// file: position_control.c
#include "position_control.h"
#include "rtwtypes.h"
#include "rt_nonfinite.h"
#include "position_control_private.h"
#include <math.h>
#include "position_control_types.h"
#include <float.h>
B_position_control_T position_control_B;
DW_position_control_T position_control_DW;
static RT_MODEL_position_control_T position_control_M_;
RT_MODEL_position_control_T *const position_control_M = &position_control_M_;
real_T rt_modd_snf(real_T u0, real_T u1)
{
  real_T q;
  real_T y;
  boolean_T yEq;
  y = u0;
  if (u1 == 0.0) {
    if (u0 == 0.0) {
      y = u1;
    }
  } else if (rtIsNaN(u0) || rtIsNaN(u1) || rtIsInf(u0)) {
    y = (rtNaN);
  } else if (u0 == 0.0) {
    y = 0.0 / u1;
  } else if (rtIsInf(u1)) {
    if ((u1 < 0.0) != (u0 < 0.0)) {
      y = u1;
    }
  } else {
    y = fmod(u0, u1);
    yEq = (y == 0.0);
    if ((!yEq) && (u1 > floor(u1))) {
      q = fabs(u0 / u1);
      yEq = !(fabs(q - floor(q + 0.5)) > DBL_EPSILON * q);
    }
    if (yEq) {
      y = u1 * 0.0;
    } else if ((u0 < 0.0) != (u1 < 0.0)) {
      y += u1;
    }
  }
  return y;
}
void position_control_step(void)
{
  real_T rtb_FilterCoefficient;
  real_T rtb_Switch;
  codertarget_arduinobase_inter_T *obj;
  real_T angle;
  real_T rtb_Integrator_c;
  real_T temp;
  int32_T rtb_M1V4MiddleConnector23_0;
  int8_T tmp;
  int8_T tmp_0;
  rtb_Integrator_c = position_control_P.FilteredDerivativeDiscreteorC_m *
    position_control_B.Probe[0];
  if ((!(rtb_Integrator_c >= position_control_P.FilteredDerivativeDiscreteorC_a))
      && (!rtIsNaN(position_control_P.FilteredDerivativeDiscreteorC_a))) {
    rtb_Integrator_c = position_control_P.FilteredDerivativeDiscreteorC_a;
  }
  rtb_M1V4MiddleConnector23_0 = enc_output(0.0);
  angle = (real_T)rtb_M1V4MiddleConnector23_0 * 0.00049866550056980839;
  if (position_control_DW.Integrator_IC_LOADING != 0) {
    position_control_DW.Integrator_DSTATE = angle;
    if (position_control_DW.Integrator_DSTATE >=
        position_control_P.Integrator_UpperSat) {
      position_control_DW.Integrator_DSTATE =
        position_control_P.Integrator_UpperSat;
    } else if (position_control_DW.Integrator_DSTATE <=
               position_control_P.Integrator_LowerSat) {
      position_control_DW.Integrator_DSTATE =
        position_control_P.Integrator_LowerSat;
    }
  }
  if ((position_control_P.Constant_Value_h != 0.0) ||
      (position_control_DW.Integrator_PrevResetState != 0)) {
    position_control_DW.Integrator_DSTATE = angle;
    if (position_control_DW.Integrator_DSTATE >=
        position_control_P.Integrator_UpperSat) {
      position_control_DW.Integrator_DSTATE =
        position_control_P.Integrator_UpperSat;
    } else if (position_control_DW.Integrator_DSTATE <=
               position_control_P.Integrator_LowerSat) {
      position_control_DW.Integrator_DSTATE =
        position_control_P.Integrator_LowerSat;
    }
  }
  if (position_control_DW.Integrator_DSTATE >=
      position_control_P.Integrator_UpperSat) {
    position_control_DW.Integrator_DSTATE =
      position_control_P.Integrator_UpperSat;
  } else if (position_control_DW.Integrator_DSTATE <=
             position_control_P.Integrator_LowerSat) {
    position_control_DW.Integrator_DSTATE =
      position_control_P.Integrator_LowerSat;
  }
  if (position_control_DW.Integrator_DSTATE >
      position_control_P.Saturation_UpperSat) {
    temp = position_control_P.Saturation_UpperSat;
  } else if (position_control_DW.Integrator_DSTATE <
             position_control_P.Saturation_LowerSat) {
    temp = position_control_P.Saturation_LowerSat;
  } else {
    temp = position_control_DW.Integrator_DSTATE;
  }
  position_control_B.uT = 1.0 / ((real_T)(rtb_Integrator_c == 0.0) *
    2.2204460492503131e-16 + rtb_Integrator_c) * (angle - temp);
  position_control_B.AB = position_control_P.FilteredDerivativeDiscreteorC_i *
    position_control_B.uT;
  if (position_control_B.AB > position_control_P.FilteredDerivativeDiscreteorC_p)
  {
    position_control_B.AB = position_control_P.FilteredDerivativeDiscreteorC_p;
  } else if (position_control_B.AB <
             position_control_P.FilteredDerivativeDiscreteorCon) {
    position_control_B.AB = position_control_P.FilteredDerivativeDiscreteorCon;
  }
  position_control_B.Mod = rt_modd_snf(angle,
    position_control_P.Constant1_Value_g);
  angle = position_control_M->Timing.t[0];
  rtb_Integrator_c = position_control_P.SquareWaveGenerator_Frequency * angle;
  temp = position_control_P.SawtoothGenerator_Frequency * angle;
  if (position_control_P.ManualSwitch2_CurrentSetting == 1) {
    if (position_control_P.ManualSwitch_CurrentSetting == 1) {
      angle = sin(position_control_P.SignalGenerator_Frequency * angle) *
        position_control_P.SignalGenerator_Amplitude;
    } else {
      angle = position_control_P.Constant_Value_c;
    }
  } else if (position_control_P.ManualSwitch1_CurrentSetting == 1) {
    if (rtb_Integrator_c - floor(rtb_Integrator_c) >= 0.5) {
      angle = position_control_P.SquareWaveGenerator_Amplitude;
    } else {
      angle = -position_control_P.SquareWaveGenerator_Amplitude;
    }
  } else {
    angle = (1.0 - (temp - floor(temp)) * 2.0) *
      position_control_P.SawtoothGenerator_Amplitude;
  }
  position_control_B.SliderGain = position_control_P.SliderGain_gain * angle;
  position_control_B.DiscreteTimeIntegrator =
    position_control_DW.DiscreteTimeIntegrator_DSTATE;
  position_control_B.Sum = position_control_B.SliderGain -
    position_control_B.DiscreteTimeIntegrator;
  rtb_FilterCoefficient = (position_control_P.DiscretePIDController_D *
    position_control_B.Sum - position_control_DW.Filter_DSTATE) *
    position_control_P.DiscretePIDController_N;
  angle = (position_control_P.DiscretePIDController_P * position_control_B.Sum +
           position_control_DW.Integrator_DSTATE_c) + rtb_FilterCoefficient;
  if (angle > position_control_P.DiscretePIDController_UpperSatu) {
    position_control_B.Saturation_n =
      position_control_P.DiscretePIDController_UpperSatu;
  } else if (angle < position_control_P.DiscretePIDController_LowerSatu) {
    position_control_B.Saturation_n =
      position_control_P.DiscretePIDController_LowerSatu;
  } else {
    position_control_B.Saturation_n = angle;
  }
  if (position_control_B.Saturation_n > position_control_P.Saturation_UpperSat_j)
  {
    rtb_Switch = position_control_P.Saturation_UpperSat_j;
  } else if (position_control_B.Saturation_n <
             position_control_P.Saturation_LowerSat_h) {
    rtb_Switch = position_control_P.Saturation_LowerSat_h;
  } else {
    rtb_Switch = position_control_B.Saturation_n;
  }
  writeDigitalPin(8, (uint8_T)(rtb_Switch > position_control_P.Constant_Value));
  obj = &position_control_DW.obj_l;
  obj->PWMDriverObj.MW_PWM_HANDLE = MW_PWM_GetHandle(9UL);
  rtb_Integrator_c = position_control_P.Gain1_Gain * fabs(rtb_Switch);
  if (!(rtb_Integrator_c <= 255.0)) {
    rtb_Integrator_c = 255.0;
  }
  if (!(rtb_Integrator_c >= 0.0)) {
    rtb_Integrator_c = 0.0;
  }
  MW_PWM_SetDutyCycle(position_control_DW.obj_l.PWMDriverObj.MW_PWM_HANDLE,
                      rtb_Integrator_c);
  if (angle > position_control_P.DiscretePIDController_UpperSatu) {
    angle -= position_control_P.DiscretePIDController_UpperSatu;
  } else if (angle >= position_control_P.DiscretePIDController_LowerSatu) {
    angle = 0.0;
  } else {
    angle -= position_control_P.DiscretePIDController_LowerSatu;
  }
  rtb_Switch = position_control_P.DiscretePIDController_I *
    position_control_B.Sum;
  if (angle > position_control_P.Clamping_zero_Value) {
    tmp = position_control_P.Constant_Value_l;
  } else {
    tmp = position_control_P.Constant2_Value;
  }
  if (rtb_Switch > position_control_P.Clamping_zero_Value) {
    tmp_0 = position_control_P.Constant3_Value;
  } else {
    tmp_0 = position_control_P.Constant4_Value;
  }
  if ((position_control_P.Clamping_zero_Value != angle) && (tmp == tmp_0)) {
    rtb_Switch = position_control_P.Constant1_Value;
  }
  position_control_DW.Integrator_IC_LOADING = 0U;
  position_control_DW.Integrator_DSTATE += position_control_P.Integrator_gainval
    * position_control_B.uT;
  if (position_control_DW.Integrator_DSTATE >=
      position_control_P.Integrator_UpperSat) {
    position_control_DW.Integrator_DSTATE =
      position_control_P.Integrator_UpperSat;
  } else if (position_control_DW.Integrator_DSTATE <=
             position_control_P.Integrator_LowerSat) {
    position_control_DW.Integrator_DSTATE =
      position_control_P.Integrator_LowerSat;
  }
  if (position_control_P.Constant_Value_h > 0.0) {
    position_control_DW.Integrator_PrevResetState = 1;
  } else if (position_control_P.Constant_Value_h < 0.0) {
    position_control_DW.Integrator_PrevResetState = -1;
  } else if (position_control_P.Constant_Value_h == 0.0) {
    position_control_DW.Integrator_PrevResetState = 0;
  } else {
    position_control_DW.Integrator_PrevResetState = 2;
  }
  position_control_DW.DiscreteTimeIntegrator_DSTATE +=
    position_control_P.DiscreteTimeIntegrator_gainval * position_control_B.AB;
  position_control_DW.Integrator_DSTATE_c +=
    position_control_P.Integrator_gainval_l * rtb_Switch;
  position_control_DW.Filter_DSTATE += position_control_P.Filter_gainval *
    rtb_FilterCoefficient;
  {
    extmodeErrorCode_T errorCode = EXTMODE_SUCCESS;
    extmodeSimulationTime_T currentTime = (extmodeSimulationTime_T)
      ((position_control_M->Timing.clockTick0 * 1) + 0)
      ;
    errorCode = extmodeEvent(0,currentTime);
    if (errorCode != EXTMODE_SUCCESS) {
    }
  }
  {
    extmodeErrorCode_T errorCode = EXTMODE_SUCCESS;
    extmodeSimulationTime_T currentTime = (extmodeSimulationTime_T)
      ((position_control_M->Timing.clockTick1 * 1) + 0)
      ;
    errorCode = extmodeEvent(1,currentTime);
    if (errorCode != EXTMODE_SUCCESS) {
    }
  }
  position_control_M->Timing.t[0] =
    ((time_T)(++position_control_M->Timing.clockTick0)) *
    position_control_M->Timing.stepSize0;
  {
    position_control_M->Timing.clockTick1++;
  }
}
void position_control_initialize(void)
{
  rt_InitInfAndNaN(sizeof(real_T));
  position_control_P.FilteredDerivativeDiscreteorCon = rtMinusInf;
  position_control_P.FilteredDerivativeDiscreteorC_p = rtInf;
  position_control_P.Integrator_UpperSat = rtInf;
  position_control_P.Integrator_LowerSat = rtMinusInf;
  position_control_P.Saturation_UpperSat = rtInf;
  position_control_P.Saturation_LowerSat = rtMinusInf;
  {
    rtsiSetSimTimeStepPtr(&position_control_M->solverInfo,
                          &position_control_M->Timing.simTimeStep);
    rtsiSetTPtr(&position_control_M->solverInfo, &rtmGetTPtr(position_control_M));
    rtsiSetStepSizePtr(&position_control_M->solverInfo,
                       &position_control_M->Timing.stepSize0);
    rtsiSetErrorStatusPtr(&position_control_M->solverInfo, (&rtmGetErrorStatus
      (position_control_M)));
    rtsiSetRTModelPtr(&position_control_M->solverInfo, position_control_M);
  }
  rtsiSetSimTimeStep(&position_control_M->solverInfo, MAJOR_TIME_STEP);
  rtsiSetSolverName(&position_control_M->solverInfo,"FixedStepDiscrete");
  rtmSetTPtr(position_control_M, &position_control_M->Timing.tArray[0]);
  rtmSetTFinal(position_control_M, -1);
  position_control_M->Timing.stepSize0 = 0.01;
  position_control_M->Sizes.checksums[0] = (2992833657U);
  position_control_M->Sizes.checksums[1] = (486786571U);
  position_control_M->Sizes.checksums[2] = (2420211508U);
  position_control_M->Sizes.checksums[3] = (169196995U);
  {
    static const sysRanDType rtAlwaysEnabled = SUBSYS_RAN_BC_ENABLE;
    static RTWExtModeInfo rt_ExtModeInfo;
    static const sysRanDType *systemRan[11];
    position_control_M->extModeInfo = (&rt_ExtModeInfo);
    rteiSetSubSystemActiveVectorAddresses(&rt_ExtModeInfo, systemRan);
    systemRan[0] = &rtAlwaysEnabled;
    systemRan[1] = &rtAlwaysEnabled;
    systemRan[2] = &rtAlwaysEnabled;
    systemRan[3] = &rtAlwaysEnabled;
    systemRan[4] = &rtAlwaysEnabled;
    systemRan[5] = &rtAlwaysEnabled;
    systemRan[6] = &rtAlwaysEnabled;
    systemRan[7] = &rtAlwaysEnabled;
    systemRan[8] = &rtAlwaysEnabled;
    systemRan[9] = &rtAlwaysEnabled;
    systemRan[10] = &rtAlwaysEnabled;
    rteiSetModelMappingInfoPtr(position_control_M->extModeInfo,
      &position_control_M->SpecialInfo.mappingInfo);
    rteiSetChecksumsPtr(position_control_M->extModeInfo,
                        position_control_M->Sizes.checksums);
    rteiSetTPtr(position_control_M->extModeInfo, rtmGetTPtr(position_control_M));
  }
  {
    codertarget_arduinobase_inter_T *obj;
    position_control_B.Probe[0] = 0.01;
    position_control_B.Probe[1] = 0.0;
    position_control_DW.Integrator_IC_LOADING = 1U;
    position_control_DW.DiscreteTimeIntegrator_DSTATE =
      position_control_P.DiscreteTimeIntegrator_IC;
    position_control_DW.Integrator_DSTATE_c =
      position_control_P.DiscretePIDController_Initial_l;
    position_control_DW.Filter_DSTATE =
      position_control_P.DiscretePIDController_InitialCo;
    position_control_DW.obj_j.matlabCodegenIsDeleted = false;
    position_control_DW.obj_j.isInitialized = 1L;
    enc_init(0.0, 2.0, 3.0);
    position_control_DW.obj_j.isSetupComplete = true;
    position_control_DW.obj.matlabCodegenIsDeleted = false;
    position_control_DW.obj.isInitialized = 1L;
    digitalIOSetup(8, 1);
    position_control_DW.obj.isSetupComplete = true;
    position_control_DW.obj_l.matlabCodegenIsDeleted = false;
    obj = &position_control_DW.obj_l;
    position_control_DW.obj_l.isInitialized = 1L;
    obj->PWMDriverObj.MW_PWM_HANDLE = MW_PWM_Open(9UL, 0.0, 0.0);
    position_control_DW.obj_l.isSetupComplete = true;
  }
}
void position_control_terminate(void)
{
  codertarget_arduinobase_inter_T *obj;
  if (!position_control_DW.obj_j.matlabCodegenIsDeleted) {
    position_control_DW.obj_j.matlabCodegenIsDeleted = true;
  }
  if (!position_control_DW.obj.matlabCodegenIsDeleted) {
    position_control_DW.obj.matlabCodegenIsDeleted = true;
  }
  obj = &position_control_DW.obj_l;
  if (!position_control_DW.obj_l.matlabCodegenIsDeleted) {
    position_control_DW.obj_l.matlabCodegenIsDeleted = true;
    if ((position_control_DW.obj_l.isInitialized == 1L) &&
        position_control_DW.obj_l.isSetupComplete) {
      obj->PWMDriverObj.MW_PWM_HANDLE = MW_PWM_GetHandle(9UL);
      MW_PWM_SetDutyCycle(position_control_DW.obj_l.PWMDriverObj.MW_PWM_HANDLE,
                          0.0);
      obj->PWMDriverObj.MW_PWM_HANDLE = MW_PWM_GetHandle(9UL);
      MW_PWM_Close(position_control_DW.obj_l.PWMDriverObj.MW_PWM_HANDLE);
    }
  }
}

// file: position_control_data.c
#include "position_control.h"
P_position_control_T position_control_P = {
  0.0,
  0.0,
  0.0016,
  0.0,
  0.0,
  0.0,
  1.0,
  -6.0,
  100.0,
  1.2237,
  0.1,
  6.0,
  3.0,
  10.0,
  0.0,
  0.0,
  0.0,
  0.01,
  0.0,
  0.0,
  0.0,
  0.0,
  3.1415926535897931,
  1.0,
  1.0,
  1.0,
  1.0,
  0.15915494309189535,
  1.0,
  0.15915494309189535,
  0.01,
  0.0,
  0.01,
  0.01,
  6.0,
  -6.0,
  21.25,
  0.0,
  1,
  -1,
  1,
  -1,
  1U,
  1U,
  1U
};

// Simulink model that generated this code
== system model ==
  Mod : Math  Operator=mod  <- 1: MATLABFunction#1, 2: Constant1
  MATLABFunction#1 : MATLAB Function  <- 1: DataTypeConversion#1
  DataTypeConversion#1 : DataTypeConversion  <- 1: M1V4MiddleConnector23
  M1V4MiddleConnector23 : MinSegLibrary_M1V4/M1V4 Middle Connector 2,3
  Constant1 : Constant  Value=pi
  DigitalOutput#1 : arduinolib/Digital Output  pinNumber=8  <- 1: CompareToZero#1
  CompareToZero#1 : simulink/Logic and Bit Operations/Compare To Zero  relop=>  <- 1: Saturation
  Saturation : Saturate  UpperLimit=6  LowerLimit=-6  <- 1: DiscretePIDController
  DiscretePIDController : slpidlib/PID Controller  Controller=PID  Form=Parallel  TimeDomain=Discrete-time  IntegratorMethod=Forward Euler  P=1.2237  I=0  D=0.0016  N=100  InitialConditionForIntegrator=0  ExternalReset=none  LimitOutput=on  UpperSaturationLimit=6  LowerSaturationLimit=-6  <- 1: Sum
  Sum : Sum  Inputs=+-  <- 1: SliderGain, 2: DiscreteTimeIntegrator
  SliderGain : simulink/Math Operations/Slider Gain  <- 1: ManualSwitch2
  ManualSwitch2 : ManualSwitch  <- 1: ManualSwitch, 2: ManualSwitch1
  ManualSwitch : ManualSwitch  <- 1: SignalGenerator, 2: Constant
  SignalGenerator : SignalGenerator
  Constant : Constant
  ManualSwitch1 : ManualSwitch  <- 1: SquareWaveGenerator, 2: SawtoothGenerator
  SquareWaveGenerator : SignalGenerator
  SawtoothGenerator : SignalGenerator
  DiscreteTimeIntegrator : DiscreteIntegrator  <- 1: FilteredDerivativeDiscreteorContinuous#1
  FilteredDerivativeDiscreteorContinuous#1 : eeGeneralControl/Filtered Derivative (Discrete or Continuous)  B=inf  A=-inf  <- 1: MATLABFunction#1
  PWM : arduinolib/PWM  pinNumber=9  <- 1: Gain1
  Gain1 : Gain  Gain=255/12  <- 1: Abs#1
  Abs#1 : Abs  <- 1: Saturation
== matlab function MATLABFunction#1 ==
function angle = count2angle(u)

N = 500; Q = 4; G = 6.3;
factor = 2 * pi / (N*Q*G);
angle = u * factor;
